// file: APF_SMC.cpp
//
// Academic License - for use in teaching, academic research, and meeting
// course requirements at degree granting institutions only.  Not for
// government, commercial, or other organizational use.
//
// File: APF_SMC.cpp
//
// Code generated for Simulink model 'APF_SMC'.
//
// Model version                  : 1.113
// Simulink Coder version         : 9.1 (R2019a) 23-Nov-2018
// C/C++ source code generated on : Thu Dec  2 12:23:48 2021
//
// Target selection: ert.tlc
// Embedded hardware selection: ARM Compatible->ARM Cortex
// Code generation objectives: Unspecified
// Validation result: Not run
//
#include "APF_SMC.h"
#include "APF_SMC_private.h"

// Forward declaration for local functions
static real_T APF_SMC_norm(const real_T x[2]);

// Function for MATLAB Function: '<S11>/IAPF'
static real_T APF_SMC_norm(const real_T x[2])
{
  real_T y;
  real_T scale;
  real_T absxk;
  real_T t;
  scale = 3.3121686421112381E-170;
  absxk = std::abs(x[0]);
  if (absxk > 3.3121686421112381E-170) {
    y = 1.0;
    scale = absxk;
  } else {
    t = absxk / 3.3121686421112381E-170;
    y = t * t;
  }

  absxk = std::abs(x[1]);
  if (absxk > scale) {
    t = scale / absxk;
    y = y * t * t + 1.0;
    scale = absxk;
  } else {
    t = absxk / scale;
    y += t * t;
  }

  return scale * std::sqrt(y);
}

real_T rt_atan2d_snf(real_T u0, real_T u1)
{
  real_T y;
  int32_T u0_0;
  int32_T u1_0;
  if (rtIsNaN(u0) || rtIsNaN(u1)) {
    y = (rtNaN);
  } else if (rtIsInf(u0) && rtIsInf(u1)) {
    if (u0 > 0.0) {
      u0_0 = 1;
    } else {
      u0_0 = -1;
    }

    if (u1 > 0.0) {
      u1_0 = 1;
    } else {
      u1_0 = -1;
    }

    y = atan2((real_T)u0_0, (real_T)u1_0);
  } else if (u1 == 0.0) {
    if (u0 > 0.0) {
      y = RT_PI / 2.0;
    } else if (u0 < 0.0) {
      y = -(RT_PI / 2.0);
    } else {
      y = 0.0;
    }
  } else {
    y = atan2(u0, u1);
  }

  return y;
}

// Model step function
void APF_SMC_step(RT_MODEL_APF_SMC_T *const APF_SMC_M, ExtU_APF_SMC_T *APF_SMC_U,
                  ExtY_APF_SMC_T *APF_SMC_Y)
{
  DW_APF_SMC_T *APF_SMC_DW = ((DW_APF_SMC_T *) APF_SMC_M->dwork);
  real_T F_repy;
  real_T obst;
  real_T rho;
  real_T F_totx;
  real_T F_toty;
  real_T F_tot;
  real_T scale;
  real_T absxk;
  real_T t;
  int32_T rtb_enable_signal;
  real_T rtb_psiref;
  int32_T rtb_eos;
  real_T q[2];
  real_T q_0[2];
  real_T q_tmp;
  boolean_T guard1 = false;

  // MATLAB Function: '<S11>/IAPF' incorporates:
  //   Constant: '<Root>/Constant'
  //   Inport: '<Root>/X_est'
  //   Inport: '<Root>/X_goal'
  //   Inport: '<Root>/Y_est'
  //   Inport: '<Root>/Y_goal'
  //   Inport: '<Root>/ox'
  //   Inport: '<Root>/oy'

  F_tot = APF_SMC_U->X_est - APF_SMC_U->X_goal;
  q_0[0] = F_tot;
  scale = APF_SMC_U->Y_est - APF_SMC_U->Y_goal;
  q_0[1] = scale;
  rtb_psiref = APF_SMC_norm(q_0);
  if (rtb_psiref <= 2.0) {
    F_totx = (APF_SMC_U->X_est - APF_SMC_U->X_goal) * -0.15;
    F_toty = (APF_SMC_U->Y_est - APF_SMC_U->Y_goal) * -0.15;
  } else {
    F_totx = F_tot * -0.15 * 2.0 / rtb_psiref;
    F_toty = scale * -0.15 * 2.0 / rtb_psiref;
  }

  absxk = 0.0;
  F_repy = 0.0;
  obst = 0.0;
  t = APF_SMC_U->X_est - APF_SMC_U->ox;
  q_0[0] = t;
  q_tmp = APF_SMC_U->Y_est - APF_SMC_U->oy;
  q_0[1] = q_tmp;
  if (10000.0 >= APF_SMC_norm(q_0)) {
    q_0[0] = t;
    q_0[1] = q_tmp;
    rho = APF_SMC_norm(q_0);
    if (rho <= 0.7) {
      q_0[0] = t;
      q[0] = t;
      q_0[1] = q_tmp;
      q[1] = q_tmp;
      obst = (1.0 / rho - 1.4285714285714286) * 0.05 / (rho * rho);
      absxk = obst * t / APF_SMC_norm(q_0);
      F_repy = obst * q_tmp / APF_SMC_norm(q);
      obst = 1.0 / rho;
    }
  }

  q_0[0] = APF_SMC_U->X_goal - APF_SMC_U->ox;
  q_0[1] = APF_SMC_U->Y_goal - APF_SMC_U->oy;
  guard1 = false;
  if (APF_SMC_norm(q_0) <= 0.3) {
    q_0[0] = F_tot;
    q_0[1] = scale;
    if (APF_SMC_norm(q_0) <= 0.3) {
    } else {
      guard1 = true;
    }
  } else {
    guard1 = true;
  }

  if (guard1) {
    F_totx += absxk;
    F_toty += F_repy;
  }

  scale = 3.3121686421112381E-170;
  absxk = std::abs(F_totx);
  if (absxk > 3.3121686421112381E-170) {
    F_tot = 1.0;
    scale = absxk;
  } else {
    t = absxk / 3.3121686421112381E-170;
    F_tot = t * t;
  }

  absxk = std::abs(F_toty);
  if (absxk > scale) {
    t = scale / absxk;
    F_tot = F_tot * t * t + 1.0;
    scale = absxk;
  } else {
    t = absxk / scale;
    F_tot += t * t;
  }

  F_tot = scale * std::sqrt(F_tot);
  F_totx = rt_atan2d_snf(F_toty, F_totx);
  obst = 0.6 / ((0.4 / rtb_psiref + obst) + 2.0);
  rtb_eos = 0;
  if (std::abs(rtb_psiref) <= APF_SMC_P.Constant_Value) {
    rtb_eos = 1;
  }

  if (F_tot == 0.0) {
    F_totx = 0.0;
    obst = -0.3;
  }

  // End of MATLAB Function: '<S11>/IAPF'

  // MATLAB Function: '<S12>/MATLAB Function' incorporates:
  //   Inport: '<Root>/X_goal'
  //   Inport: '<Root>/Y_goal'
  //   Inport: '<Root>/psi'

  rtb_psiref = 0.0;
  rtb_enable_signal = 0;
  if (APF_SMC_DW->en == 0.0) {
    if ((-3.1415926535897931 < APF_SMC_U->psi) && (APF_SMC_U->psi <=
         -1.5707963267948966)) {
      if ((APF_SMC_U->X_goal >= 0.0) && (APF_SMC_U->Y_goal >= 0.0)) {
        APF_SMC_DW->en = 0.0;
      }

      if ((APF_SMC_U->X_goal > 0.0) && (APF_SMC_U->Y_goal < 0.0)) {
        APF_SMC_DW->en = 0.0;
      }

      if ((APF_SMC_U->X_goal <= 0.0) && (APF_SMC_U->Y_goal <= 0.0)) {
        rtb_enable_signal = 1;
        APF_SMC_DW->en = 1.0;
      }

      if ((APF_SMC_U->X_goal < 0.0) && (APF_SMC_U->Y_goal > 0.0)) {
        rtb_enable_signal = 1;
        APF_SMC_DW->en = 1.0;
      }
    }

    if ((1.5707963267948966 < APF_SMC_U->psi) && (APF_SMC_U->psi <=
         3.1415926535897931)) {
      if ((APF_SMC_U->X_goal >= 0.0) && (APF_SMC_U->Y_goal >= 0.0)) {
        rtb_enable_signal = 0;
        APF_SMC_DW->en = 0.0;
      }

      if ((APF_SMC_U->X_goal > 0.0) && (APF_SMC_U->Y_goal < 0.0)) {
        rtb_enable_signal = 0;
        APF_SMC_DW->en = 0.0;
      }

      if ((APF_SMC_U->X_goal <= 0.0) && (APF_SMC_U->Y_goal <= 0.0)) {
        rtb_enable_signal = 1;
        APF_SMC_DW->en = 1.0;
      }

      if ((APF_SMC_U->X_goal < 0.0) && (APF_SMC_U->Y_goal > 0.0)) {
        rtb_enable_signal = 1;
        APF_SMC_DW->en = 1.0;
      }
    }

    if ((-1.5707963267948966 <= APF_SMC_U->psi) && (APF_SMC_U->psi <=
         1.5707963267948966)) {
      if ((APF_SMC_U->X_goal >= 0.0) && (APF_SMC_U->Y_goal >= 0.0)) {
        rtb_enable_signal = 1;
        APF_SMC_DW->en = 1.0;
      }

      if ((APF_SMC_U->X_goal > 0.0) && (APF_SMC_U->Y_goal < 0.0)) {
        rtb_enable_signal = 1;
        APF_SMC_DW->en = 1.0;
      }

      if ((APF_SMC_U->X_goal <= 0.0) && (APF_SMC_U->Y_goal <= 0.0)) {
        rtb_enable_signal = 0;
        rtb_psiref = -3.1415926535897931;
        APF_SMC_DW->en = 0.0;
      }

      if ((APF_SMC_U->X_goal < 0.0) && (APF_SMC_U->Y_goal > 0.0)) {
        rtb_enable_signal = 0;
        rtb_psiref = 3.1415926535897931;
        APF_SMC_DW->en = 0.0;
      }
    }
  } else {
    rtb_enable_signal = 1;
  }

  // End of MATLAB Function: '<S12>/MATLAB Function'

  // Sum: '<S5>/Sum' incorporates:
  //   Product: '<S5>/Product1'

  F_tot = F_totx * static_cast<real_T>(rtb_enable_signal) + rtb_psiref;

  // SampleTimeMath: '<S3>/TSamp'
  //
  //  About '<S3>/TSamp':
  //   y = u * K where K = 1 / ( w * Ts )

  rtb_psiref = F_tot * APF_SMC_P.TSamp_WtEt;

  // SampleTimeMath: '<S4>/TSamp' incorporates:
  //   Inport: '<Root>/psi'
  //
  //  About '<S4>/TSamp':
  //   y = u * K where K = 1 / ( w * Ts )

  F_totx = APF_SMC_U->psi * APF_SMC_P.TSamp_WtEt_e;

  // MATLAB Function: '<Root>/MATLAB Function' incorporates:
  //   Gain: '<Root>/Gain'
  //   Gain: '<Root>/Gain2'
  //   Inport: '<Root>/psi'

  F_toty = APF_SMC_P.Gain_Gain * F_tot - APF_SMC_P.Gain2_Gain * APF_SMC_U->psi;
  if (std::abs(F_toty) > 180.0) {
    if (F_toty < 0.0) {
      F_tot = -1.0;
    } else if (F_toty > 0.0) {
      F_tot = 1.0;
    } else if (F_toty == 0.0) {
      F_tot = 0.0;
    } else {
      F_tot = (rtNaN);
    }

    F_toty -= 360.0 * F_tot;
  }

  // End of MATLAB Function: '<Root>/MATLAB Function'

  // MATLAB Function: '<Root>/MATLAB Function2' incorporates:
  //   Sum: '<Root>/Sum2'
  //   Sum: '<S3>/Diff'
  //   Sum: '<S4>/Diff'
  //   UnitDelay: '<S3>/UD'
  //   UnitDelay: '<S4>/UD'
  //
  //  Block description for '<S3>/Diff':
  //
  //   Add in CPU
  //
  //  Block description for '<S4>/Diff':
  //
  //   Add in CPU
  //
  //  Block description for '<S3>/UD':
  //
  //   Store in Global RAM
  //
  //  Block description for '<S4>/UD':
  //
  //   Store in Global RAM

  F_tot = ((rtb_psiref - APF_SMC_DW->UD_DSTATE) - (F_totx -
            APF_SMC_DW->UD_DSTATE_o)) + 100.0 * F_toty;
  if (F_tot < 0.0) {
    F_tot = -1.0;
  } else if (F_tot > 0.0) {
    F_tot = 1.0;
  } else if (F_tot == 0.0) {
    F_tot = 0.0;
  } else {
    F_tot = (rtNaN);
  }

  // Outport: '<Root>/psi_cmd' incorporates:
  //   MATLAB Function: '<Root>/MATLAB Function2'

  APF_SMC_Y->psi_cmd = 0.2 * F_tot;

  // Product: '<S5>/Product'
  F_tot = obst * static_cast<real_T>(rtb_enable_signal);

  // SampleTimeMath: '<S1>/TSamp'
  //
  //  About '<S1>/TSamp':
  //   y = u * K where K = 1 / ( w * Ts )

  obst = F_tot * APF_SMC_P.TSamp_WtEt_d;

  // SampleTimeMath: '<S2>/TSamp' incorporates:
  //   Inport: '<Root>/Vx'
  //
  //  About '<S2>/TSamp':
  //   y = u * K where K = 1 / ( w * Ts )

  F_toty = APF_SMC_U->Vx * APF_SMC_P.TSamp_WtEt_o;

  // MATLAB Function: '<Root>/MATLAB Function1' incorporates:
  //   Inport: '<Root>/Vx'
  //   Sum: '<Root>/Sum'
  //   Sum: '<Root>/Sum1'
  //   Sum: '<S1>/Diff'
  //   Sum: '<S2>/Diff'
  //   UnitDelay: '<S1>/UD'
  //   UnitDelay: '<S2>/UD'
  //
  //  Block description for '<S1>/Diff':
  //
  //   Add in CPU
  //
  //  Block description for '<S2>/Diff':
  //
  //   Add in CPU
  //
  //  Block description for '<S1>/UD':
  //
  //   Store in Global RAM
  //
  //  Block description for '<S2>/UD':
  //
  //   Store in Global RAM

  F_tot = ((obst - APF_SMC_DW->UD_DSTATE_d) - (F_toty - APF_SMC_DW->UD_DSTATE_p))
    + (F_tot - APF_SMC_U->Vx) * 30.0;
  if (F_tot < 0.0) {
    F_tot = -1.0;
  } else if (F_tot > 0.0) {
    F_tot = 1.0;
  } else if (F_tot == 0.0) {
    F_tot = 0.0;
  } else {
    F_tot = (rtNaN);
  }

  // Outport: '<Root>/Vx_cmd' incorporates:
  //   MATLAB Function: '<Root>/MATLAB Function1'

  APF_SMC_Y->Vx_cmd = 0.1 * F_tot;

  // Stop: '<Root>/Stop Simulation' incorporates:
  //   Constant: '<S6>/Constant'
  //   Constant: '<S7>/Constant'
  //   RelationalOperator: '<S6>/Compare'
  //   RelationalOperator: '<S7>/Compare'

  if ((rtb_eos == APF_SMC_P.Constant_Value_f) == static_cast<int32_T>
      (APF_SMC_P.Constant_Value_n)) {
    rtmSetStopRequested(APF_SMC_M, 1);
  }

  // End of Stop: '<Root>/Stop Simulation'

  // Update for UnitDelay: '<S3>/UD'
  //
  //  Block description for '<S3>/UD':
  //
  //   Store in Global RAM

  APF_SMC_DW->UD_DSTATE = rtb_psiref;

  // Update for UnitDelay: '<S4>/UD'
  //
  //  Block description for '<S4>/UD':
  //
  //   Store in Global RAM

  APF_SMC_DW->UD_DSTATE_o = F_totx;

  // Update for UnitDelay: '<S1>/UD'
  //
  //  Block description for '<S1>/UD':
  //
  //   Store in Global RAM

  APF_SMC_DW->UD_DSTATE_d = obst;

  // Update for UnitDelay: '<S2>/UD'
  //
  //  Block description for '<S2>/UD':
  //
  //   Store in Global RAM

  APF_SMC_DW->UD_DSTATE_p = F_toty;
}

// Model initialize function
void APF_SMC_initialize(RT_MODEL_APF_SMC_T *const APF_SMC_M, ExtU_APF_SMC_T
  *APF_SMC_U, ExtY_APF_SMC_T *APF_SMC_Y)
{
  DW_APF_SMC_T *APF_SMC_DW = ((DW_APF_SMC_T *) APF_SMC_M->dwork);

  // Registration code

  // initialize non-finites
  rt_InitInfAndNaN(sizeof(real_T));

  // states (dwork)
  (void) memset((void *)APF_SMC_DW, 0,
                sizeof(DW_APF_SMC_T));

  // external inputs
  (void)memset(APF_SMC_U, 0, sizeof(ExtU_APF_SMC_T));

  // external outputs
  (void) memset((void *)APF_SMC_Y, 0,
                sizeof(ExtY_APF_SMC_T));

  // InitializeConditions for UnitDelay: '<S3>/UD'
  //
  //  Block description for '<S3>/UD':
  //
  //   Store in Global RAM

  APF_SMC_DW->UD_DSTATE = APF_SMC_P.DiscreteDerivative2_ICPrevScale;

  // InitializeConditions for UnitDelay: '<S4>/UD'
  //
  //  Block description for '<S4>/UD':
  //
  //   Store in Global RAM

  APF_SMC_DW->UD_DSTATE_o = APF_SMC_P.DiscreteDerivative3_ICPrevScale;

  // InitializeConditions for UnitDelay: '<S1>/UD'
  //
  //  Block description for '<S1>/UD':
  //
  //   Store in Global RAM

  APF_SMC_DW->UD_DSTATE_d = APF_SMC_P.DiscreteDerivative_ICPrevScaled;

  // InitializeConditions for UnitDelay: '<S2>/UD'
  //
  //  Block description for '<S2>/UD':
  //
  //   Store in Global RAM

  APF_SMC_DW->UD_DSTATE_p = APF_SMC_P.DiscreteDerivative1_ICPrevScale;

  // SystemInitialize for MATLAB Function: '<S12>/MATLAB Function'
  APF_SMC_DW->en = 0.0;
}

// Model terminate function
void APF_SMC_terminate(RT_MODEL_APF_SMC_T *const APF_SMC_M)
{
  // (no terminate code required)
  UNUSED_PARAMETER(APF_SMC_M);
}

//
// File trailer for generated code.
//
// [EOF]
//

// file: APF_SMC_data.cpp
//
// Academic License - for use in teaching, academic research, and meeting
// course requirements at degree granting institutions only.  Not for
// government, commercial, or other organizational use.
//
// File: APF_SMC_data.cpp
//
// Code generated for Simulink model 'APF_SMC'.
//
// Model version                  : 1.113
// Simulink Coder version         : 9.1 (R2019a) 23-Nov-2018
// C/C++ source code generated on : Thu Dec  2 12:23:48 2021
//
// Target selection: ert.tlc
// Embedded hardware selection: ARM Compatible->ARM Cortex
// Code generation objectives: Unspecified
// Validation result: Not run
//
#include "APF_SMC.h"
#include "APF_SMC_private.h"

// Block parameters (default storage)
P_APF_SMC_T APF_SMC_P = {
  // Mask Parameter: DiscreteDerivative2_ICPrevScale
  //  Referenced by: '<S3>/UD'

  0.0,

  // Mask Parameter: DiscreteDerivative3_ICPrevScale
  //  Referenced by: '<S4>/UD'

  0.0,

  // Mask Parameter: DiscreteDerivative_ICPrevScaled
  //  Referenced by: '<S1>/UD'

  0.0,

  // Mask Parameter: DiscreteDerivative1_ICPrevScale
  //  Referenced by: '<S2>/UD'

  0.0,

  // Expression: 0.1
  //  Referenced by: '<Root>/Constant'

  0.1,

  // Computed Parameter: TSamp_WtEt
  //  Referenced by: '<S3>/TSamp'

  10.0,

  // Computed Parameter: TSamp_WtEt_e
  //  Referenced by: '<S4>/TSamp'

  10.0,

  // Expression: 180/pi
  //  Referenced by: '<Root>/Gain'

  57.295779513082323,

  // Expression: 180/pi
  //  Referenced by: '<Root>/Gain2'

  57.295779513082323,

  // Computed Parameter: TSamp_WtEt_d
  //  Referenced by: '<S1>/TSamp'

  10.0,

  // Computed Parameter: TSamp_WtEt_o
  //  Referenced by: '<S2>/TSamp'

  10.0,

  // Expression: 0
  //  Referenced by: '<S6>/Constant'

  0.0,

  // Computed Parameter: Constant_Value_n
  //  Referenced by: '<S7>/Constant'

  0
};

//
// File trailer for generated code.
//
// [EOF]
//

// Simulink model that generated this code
simulink model "APF_SMC"  (R2019a)
settings: Solver=FixedStepDiscrete  StartTime=0.0  StopTime=60  FixedStep=0.1  RelTol=1e-3
undefined symbols (not defined in the file): Kd_psi, Kd_Vx, Ki_psi, Ki_Vx, Kp_psi, Kp_Vx
libraries: simulink x8

== system APF_SMC ==
  psi : Inport
  Vx : Inport  Port=2
  X_est : Inport  Port=3
  Y_est : Inport  Port=4
  X_goal : Inport  Port=5
  Y_goal : Inport  Port=6
  ox : Inport  Port=7
  oy : Inport  Port=8
  1/180 : Gain  Commented=on  Gain=1/180
  Constant : Constant  Value=0.1
  Discrete Derivative{,1..3} (4 alike) : simulink/Discrete/Discrete Derivative  gainval=1.0  ICPrevScaledInput=0.0  OutMin=[]  OutMax=[]  OutDataType=fixdt(1, 16)  OutScaling=2^-10  DoSatur=off
  "GUIDANCE " : Subsystem
  Gain : Gain  Gain=180/pi
  Gain2 : Gain  Gain=180/pi
  IsNonZero : simulink/Logic and Bit Operations/Compare To Zero  relop===  OutDataTypeStr=boolean
  IsZero : simulink/Logic and Bit Operations/Compare To Zero  relop===  OutDataTypeStr=boolean
  MATLAB Function : MATLAB Function  TreatAsAtomicUnit=on
  MATLAB Function1 : MATLAB Function  TreatAsAtomicUnit=on
  MATLAB Function2 : MATLAB Function  TreatAsAtomicUnit=on
  PID Controller : simulink/Continuous/PID Controller  Commented=on  Controller=PID  Form=Parallel  TimeDomain=Continuous-time  SampleTime=-1  IntegratorMethod=Forward Euler  FilterMethod=Forward Euler  ControllerParametersSource=internal  P=Kp_Vx  I=Ki_Vx  D=Kd_Vx  UseFilter=on  N=100  TunerSelectOption=Transfer Function Based (PID Tuner App)  InitialConditionSource=internal  InitialConditionForIntegrator=0  InitialConditionForFilter=0  DifferentiatorICPrevScaledInput=0  ExternalReset=none  TrackingMode=off  Kt=1  LimitOutput=off  UpperSaturationLimit=inf  LowerSaturationLimit=-inf  LinearizeAsGain=on  AntiWindupMode=none  Kb=1  POutMin=[]  POutMax=[]  IOutMin=[]  IOutMax=[]  DOutMin=[]  DOutMax=[]  NOutMin=[]  NOutMax=[]  SumOutMin=[]  SumOutMax=[]  SaturationOutMin=[]  SaturationOutMax=[]  PParamMin=[]  PParamMax=[]  IParamMin=[]  IParamMax=[]  DParamMin=[]  DParamMax=[]  NParamMin=[]  NParamMax=[]  KbParamMin=[]  KbParamMax=[]  KtParamMin=[]  KtParamMax=[]  KbOutMin=[]  KbOutMax=[]  KtOutMin=[]  KtOutMax=[]  IntegratorOutMin=[]  IntegratorOutMax=[]  FilterOutMin=[]  FilterOutMax=[]  SumI1OutMin=[]  SumI1OutMax=[]  SumI2OutMin=[]  SumI2OutMax=[]  SumI3OutMin=[]  SumI3OutMax=[]  SumI4OutMin=[]  SumI4OutMax=[]  SumDOutMin=[]  SumDOutMax=[]  DifferentiatorOutMin=[]  DifferentiatorOutMax=[]  FilterDiffOutCoefMin=[]  FilterDiffOutCoefMax=[]  ReciprocalOutMin=[]  ReciprocalOutMax=[]  SumDenOutMin=[]  SumDenOutMax=[]  SumNumOutMin=[]  SumNumOutMax=[]  DivideOutMin=[]  DivideOutMax=[]  IntegratorContinuousStateAttributes=''  IntegratorStateMustResolveToSignalObject=off  IntegratorRTWStateStorageClass=Auto  FilterContinuousStateAttributes=''  FilterStateMustResolveToSignalObject=off  FilterRTWStateStorageClass=Auto  ParallelPVariant=InternalParameters  IdealPVariant=Disabled  IVariant=InternalParameters  DVariant=InternalParameters  IntegratorVariant=Continuous  SatVariant=Disabled  AWVariant=Passthrough  PCopyVariant=Disabled  TRVariant=Disabled  FdbkBlocksVariant=Forward  IdealPFdbkVariant=Disabled  SatFdbkVariant=Disabled  DerivativeFilterVariant=ContFilter  NVariant=InternalParameters  NCopyVariant=Disabled  FilterICVariant=InternalICsFilter  IntegratorICVariant=InternalICs  ExternalResetVariant=Disabled  TRSumVariant=Passthrough  SumFdbkVariant=Disabled  SumVariant=Sum_PID
  PID Controller1 : simulink/Continuous/PID Controller  Commented=on  Controller=PID  Form=Parallel  TimeDomain=Continuous-time  SampleTime=-1  IntegratorMethod=Forward Euler  FilterMethod=Forward Euler  ControllerParametersSource=internal  P=Kp_psi  I=Ki_psi  D=Kd_psi  UseFilter=on  N=100  TunerSelectOption=Transfer Function Based (PID Tuner App)  InitialConditionSource=internal  InitialConditionForIntegrator=0  InitialConditionForFilter=0  DifferentiatorICPrevScaledInput=0  ExternalReset=none  TrackingMode=off  Kt=1  LimitOutput=off  UpperSaturationLimit=inf  LowerSaturationLimit=-inf  LinearizeAsGain=on  AntiWindupMode=none  Kb=1  POutMin=[]  POutMax=[]  IOutMin=[]  IOutMax=[]  DOutMin=[]  DOutMax=[]  NOutMin=[]  NOutMax=[]  SumOutMin=[]  SumOutMax=[]  SaturationOutMin=[]  SaturationOutMax=[]  PParamMin=[]  PParamMax=[]  IParamMin=[]  IParamMax=[]  DParamMin=[]  DParamMax=[]  NParamMin=[]  NParamMax=[]  KbParamMin=[]  KbParamMax=[]  KtParamMin=[]  KtParamMax=[]  KbOutMin=[]  KbOutMax=[]  KtOutMin=[]  KtOutMax=[]  IntegratorOutMin=[]  IntegratorOutMax=[]  FilterOutMin=[]  FilterOutMax=[]  SumI1OutMin=[]  SumI1OutMax=[]  SumI2OutMin=[]  SumI2OutMax=[]  SumI3OutMin=[]  SumI3OutMax=[]  SumI4OutMin=[]  SumI4OutMax=[]  SumDOutMin=[]  SumDOutMax=[]  DifferentiatorOutMin=[]  DifferentiatorOutMax=[]  FilterDiffOutCoefMin=[]  FilterDiffOutCoefMax=[]  ReciprocalOutMin=[]  ReciprocalOutMax=[]  SumDenOutMin=[]  SumDenOutMax=[]  SumNumOutMin=[]  SumNumOutMax=[]  DivideOutMin=[]  DivideOutMax=[]  IntegratorContinuousStateAttributes=''  IntegratorStateMustResolveToSignalObject=off  IntegratorRTWStateStorageClass=Auto  FilterContinuousStateAttributes=''  FilterStateMustResolveToSignalObject=off  FilterRTWStateStorageClass=Auto  ParallelPVariant=InternalParameters  IdealPVariant=Disabled  IVariant=InternalParameters  DVariant=InternalParameters  IntegratorVariant=Continuous  SatVariant=Disabled  AWVariant=Passthrough  PCopyVariant=Disabled  TRVariant=Disabled  FdbkBlocksVariant=Forward  IdealPFdbkVariant=Disabled  SatFdbkVariant=Disabled  DerivativeFilterVariant=ContFilter  NVariant=InternalParameters  NCopyVariant=Disabled  FilterICVariant=InternalICsFilter  IntegratorICVariant=InternalICs  ExternalResetVariant=Disabled  TRSumVariant=Passthrough  SumFdbkVariant=Disabled  SumVariant=Sum_PID
  Product : Product  Commented=on
  Product1 : Product  Commented=on
  Rate Transition : RateTransition
  Rate Transition1 : RateTransition
  Saturation : Saturate  Commented=on
  Saturation1 : Saturate  Commented=on  UpperLimit=1  LowerLimit=-1
  Scope : Scope  NumInputPorts=2
  Scope1 : Scope  NumInputPorts=2
  Scope2 : Scope  NumInputPorts=2
  Stop Simulation : Stop
  Sum : Sum  Inputs=|+-
  Sum1 : Sum  Inputs=|+-
  Sum2 : Sum  Inputs=|+-
  Terminator : Terminator  Commented=on
  Terminator1 : Terminator  Commented=on
  To Workspace1 : ToWorkspace  VariableName=Vx_ref  SaveFormat=Structure With Time  SampleTime=-1
  To Workspace5 : ToWorkspace  VariableName=psi_ref  SaveFormat=Structure With Time  SampleTime=-1
  Vx_cmd : Outport  VectorParamsAs1DForOutWhenUnconnected=on
  psi_cmd : Outport  Port=2  VectorParamsAs1DForOutWhenUnconnected=on
  wires:
  Gain/1 -> Scope1/1, MATLAB Function/1(psi_ref)  "psi_ref"
  Gain2/1 -> Scope1/2, MATLAB Function/2(psi_est)  "psi"
  "GUIDANCE "/3(eos) -> IsNonZero/1
  1/180/1 -> Saturation/1  "psi_cmd"
  Discrete Derivative2/1 -> Sum2/1  "psidot_ref"
  Product1/1 -> Terminator1/1
  Product/1 -> Terminator/1
  IsNonZero/1 -> IsZero/1, Product1/2, Product/2
  Sum2/1 -> MATLAB Function2/1(psidot_error)  "psidot_err"
  X_goal/1 -> "GUIDANCE "/3(X_goal)
  MATLAB Function2/1(psi_cmd) -> psi_cmd/1, Scope2/2
  IsZero/1 -> Stop Simulation/1
  Constant/1 -> "GUIDANCE "/8(Toll_to_end)
  Discrete Derivative3/1 -> Sum2/2  "psidot"
  Rate Transition/1 -> To Workspace5/1
  Y_est/1 -> "GUIDANCE "/2(Y_est)
  Saturation1/1 -> Product1/1
  X_est/1 -> "GUIDANCE "/1(X_est)
  MATLAB Function/1(errore) -> PID Controller1/1, MATLAB Function2/2(psi_error)  "psi_error"
  PID Controller/1 -> Saturation1/1
  ox/1 -> "GUIDANCE "/5(ox)
  oy/1 -> "GUIDANCE "/6(oy)
  Sum/1 -> PID Controller/1, MATLAB Function1/2(Vx_err)  "Vx_err"
  MATLAB Function1/1(Vx_cmd) -> Scope2/1, Vx_cmd/1
  Saturation/1 -> Product/1
  Discrete Derivative1/1 -> Sum1/2  "Ax"
  "GUIDANCE "/1(Vx_ref) -> Rate Transition1/1, Scope/1, Sum/1, Discrete Derivative/1
  Y_goal/1 -> "GUIDANCE "/4(Y_goal)
  PID Controller1/1 -> 1/180/1
  Vx/1 -> Scope/2, Sum/2, Discrete Derivative1/1
  Discrete Derivative/1 -> Sum1/1  "Ax_ref"
  Rate Transition1/1 -> To Workspace1/1
  Sum1/1 -> MATLAB Function1/1(Ax_err)  "Ax_err"
  psi/1 -> "GUIDANCE "/7(psi_est), Discrete Derivative3/1, Gain2/1
  "GUIDANCE "/2(psi_ref) -> Discrete Derivative2/1, Gain/1, Rate Transition/1

== system APF_SMC/GUIDANCE  ==
  X_est : Inport
  Y_est : Inport  Port=2
  X_goal : Inport  Port=3
  Y_goal : Inport  Port=4
  ox : Inport  Port=5
  oy : Inport  Port=6
  psi_est : Inport  Port=7
  Toll_to_end : Inport  Port=8
  APF : Subsystem
  INITIAL ORIENTATION : Subsystem
  Product : Product
  Product1 : Product
  Sum : Sum  Inputs=|++
  Vx_ref : Outport  VectorParamsAs1DForOutWhenUnconnected=on
  psi_ref : Outport  Port=2  VectorParamsAs1DForOutWhenUnconnected=on
  eos : Outport  Port=3  VectorParamsAs1DForOutWhenUnconnected=on
  wires:
  X_goal/1 -> INITIAL ORIENTATION/1(X_goal), APF/3(X_goal)
  Y_goal/1 -> INITIAL ORIENTATION/2(Y_goal), APF/4(Y_goal)
  X_est/1 -> APF/1(X_est)
  Y_est/1 -> APF/2(Y_est)
  ox/1 -> APF/5(ox)
  oy/1 -> APF/6(oy)
  Sum/1 -> psi_ref/1
  psi_est/1 -> INITIAL ORIENTATION/3(psi_est)
  INITIAL ORIENTATION/2(psiref) -> Sum/2
  APF/1(V_ref) -> Product/1
  Product/1 -> Vx_ref/1
  INITIAL ORIENTATION/1(enable_signal) -> Product1/2, Product/2
  APF/2(psi_ref) -> Product1/1
  Product1/1 -> Sum/1
  APF/3(eos) -> eos/1
  Toll_to_end/1 -> APF/7(Toll_to_end)

== system APF_SMC/GUIDANCE /APF ==
  X_est : Inport
  Y_est : Inport  Port=2
  X_goal : Inport  Port=3
  Y_goal : Inport  Port=4
  ox : Inport  Port=5
  oy : Inport  Port=6
  Toll_to_end : Inport  Port=7
  IAPF : MATLAB Function  TreatAsAtomicUnit=on
  Scope1 : Scope  NumInputPorts=2
  Scope3 : Scope
  Scope4 : Scope  NumInputPorts=2
  V_ref : Outport  VectorParamsAs1DForOutWhenUnconnected=on
  psi_ref : Outport  Port=2  VectorParamsAs1DForOutWhenUnconnected=on
  eos : Outport  Port=3  VectorParamsAs1DForOutWhenUnconnected=on
  wires:
  IAPF/1(V_ref) -> V_ref/1
  IAPF/6(F_attx) -> Scope1/2
  IAPF/3(rho_goal) -> Scope3/1
  IAPF/4(F_repx) -> Scope1/1
  IAPF/7(F_atty) -> Scope4/2
  IAPF/5(F_repy) -> Scope4/1
  X_est/1 -> IAPF/1(X_est)
  ox/1 -> IAPF/5(ox)
  IAPF/2(psi_ref) -> psi_ref/1
  Y_est/1 -> IAPF/2(Y_est)
  oy/1 -> IAPF/6(oy)
  IAPF/8(eos) -> eos/1
  X_goal/1 -> IAPF/3(X_goal)
  Y_goal/1 -> IAPF/4(Y_goal)
  Toll_to_end/1 -> IAPF/7(Toll_to_end)

== system APF_SMC/GUIDANCE /INITIAL ORIENTATION ==
  X_goal : Inport
  Y_goal : Inport  Port=2
  psi_est : Inport  Port=3
  MATLAB Function : MATLAB Function  TreatAsAtomicUnit=on
  enable_signal : Outport  VectorParamsAs1DForOutWhenUnconnected=on
  psiref : Outport  Port=2  VectorParamsAs1DForOutWhenUnconnected=on
  wires:
  psi_est/1 -> MATLAB Function/3(psi_est)
  MATLAB Function/2(psiref) -> psiref/1
  Y_goal/1 -> MATLAB Function/2(Y_goal)
  X_goal/1 -> MATLAB Function/1(X_goal)
  MATLAB Function/1(enable_signal) -> enable_signal/1

== matlab function APF_SMC/GUIDANCE /INITIAL ORIENTATION/MATLAB Function ==
function [enable_signal, psiref] = fcn(X_goal, Y_goal, psi_est)
psiref=0;
enable_signal=0;

persistent en
if isempty(en)
    en=0;
end

if en==0
if -pi<psi_est && psi_est<=-pi/2 
  if X_goal>=0 && Y_goal>=0
      enable_signal=0;
      psiref=0;
      en=0;
  end
   if X_goal>0 && Y_goal<0
      enable_signal=0;
      psiref=0;
      en=0;
   end
    if X_goal<=0 && Y_goal<=0
      enable_signal=1;
      en=1;
      psiref=0;
    end
    if X_goal<0 && Y_goal>0
      enable_signal=1;
      en=1;
      psiref=0;
    end
end
if pi/2<psi_est && psi_est<=pi 
  if X_goal>=0 && Y_goal>=0
      enable_signal=0;
      psiref=0;
      en=0;
  end
   if X_goal>0 && Y_goal<0
      enable_signal=0;
      psiref=0;
      en=0;
   end
    if X_goal<=0 && Y_goal<=0
      enable_signal=1;
      en=1;
      psiref=0;
    end
    if X_goal<0 && Y_goal>0
      enable_signal=1;
      en=1;
      psiref=0;
    end
end

if -pi/2<=psi_est && psi_est<=pi/2
  if X_goal>=0 && Y_goal>=0
      enable_signal=1;
      en=1;
      psiref=0;
  end
   if X_goal>0 && Y_goal<0
      enable_signal=1;
      en=1;
      psiref=0;
   end
    if X_goal<=0 && Y_goal<=0
      enable_signal=0;
      psiref=-pi;
      en=0;
    end
    if X_goal<0 && Y_goal>0
      enable_signal=0;
      psiref=pi;
      en=0;
    end
end
else
    enable_signal=1;
    psiref=0;
end

== matlab function APF_SMC/MATLAB Function1 ==
function Vx_cmd = SMC_Vx(Ax_err, Vx_err)
% SMC params
lamda = 30;
K = 0.1;
% Sliding surface
s = zeros(1);
s = (Ax_err) + lamda*(Vx_err);

Vx_cmd = K*sign(s);

== matlab function APF_SMC/MATLAB Function ==
function errore = fcn(psi_ref, psi_est)
errore=psi_ref-psi_est;

if abs(errore)>180
    errore=errore-360*sign(errore);
end

== matlab function APF_SMC/GUIDANCE /APF/IAPF ==
function [V_ref, psi_ref, rho_goal, F_repx, F_repy, F_attx, F_atty, eos]  = fcn(X_est, Y_est, X_goal, Y_goal,  ox, oy, Toll_to_end)

% Potential field characteristics
rho_0=0.7;                   % Area of influence of obstacle  [m]
kp = 0.15;                   % Attractive pottential gain
eta = 0.05;                  % Repulsive potential gain

q=[X_est, Y_est]';           % Actual position [m]       
qg=[X_goal, Y_goal]';        % Goal position   [m]
rho_goal=norm(q-qg,2);       % Distance actual position-goal position
d=2;                         % Distance from goal, point of attractive field characteristic switching

% ATTRACTIVE
if rho_goal<=d
F_attx = -kp*(X_est-X_goal);
F_atty = -kp*(Y_est-Y_goal);
else    
F_attx = -kp*(X_est-X_goal)*d/rho_goal;
F_atty = -kp*(Y_est-Y_goal)*d/rho_goal;
end

% REPULSIVE
F_repx=0;
F_repy=0;
dmin=10000;
qc=[0 0]';
obst=0;

for k=1:length(ox)
    qc=[ox(k) oy(k)]';                          % Obstacle position [m]
    dq = norm(q-qc,2);                          % Distance actual position- obstacle position
     
    if dmin >= dq
        dmin = dq;
        min_ost = k;
        qc=[ox(min_ost) oy(min_ost)]';
        rho = norm(q-qc,2) ;                    % Distance with the nearest obstacle
        
        if rho<=rho_0                           % Inside obstacle area! Danger
           F_repx=eta*(1/rho - 1/rho_0)*1/(rho).^2*(X_est-ox(min_ost))/norm(q-qc,2);
           F_repy=eta*(1/rho - 1/rho_0)*1/(rho).^2*(Y_est-oy(min_ost))/norm(q-qc,2);  
           obst=1/rho;
        end
     
     end
end

% To find the goal if the obstacle is near
dob=0.3;
dgr=0.3;

if norm(qg-qc,2)<=dob && norm(q-qg,2)<=dgr
    F_totx=F_attx;
    F_toty=F_atty;
else
    F_totx = F_attx+F_repx;
    F_toty = F_atty+F_repy;
end

% Potential Force
F_tot=norm([F_totx,F_toty]);

% ORIENTATION REFERENCE SIGNAL
psi_ref=atan2(F_toty,F_totx);

% VELOCITY REFERENCE SIGNAL
% 1° prova per il campo di velocità
% V_ref=F_totx/F_tot*0.3;

% 2° prova per il campo di velocità
delta=0.4/rho_goal+obst;
V_ref= 0.3*2/(2+delta);

eos = 0;
% END OF SIMULATION
if abs(rho_goal)<=Toll_to_end
    eos=1;
end

% Mathematical minimum
if F_tot==0
    psi_ref=0;
    V_ref=-0.3;
end

== matlab function APF_SMC/MATLAB Function2 ==
function psi_cmd = SMC_psi(psidot_error, psi_error)
% SMC params
lamda = 100;
K = 0.2;
% Sliding surface
s = zeros(1);
s = (psidot_error) + lamda*(psi_error);

psi_cmd = K*sign(s);
